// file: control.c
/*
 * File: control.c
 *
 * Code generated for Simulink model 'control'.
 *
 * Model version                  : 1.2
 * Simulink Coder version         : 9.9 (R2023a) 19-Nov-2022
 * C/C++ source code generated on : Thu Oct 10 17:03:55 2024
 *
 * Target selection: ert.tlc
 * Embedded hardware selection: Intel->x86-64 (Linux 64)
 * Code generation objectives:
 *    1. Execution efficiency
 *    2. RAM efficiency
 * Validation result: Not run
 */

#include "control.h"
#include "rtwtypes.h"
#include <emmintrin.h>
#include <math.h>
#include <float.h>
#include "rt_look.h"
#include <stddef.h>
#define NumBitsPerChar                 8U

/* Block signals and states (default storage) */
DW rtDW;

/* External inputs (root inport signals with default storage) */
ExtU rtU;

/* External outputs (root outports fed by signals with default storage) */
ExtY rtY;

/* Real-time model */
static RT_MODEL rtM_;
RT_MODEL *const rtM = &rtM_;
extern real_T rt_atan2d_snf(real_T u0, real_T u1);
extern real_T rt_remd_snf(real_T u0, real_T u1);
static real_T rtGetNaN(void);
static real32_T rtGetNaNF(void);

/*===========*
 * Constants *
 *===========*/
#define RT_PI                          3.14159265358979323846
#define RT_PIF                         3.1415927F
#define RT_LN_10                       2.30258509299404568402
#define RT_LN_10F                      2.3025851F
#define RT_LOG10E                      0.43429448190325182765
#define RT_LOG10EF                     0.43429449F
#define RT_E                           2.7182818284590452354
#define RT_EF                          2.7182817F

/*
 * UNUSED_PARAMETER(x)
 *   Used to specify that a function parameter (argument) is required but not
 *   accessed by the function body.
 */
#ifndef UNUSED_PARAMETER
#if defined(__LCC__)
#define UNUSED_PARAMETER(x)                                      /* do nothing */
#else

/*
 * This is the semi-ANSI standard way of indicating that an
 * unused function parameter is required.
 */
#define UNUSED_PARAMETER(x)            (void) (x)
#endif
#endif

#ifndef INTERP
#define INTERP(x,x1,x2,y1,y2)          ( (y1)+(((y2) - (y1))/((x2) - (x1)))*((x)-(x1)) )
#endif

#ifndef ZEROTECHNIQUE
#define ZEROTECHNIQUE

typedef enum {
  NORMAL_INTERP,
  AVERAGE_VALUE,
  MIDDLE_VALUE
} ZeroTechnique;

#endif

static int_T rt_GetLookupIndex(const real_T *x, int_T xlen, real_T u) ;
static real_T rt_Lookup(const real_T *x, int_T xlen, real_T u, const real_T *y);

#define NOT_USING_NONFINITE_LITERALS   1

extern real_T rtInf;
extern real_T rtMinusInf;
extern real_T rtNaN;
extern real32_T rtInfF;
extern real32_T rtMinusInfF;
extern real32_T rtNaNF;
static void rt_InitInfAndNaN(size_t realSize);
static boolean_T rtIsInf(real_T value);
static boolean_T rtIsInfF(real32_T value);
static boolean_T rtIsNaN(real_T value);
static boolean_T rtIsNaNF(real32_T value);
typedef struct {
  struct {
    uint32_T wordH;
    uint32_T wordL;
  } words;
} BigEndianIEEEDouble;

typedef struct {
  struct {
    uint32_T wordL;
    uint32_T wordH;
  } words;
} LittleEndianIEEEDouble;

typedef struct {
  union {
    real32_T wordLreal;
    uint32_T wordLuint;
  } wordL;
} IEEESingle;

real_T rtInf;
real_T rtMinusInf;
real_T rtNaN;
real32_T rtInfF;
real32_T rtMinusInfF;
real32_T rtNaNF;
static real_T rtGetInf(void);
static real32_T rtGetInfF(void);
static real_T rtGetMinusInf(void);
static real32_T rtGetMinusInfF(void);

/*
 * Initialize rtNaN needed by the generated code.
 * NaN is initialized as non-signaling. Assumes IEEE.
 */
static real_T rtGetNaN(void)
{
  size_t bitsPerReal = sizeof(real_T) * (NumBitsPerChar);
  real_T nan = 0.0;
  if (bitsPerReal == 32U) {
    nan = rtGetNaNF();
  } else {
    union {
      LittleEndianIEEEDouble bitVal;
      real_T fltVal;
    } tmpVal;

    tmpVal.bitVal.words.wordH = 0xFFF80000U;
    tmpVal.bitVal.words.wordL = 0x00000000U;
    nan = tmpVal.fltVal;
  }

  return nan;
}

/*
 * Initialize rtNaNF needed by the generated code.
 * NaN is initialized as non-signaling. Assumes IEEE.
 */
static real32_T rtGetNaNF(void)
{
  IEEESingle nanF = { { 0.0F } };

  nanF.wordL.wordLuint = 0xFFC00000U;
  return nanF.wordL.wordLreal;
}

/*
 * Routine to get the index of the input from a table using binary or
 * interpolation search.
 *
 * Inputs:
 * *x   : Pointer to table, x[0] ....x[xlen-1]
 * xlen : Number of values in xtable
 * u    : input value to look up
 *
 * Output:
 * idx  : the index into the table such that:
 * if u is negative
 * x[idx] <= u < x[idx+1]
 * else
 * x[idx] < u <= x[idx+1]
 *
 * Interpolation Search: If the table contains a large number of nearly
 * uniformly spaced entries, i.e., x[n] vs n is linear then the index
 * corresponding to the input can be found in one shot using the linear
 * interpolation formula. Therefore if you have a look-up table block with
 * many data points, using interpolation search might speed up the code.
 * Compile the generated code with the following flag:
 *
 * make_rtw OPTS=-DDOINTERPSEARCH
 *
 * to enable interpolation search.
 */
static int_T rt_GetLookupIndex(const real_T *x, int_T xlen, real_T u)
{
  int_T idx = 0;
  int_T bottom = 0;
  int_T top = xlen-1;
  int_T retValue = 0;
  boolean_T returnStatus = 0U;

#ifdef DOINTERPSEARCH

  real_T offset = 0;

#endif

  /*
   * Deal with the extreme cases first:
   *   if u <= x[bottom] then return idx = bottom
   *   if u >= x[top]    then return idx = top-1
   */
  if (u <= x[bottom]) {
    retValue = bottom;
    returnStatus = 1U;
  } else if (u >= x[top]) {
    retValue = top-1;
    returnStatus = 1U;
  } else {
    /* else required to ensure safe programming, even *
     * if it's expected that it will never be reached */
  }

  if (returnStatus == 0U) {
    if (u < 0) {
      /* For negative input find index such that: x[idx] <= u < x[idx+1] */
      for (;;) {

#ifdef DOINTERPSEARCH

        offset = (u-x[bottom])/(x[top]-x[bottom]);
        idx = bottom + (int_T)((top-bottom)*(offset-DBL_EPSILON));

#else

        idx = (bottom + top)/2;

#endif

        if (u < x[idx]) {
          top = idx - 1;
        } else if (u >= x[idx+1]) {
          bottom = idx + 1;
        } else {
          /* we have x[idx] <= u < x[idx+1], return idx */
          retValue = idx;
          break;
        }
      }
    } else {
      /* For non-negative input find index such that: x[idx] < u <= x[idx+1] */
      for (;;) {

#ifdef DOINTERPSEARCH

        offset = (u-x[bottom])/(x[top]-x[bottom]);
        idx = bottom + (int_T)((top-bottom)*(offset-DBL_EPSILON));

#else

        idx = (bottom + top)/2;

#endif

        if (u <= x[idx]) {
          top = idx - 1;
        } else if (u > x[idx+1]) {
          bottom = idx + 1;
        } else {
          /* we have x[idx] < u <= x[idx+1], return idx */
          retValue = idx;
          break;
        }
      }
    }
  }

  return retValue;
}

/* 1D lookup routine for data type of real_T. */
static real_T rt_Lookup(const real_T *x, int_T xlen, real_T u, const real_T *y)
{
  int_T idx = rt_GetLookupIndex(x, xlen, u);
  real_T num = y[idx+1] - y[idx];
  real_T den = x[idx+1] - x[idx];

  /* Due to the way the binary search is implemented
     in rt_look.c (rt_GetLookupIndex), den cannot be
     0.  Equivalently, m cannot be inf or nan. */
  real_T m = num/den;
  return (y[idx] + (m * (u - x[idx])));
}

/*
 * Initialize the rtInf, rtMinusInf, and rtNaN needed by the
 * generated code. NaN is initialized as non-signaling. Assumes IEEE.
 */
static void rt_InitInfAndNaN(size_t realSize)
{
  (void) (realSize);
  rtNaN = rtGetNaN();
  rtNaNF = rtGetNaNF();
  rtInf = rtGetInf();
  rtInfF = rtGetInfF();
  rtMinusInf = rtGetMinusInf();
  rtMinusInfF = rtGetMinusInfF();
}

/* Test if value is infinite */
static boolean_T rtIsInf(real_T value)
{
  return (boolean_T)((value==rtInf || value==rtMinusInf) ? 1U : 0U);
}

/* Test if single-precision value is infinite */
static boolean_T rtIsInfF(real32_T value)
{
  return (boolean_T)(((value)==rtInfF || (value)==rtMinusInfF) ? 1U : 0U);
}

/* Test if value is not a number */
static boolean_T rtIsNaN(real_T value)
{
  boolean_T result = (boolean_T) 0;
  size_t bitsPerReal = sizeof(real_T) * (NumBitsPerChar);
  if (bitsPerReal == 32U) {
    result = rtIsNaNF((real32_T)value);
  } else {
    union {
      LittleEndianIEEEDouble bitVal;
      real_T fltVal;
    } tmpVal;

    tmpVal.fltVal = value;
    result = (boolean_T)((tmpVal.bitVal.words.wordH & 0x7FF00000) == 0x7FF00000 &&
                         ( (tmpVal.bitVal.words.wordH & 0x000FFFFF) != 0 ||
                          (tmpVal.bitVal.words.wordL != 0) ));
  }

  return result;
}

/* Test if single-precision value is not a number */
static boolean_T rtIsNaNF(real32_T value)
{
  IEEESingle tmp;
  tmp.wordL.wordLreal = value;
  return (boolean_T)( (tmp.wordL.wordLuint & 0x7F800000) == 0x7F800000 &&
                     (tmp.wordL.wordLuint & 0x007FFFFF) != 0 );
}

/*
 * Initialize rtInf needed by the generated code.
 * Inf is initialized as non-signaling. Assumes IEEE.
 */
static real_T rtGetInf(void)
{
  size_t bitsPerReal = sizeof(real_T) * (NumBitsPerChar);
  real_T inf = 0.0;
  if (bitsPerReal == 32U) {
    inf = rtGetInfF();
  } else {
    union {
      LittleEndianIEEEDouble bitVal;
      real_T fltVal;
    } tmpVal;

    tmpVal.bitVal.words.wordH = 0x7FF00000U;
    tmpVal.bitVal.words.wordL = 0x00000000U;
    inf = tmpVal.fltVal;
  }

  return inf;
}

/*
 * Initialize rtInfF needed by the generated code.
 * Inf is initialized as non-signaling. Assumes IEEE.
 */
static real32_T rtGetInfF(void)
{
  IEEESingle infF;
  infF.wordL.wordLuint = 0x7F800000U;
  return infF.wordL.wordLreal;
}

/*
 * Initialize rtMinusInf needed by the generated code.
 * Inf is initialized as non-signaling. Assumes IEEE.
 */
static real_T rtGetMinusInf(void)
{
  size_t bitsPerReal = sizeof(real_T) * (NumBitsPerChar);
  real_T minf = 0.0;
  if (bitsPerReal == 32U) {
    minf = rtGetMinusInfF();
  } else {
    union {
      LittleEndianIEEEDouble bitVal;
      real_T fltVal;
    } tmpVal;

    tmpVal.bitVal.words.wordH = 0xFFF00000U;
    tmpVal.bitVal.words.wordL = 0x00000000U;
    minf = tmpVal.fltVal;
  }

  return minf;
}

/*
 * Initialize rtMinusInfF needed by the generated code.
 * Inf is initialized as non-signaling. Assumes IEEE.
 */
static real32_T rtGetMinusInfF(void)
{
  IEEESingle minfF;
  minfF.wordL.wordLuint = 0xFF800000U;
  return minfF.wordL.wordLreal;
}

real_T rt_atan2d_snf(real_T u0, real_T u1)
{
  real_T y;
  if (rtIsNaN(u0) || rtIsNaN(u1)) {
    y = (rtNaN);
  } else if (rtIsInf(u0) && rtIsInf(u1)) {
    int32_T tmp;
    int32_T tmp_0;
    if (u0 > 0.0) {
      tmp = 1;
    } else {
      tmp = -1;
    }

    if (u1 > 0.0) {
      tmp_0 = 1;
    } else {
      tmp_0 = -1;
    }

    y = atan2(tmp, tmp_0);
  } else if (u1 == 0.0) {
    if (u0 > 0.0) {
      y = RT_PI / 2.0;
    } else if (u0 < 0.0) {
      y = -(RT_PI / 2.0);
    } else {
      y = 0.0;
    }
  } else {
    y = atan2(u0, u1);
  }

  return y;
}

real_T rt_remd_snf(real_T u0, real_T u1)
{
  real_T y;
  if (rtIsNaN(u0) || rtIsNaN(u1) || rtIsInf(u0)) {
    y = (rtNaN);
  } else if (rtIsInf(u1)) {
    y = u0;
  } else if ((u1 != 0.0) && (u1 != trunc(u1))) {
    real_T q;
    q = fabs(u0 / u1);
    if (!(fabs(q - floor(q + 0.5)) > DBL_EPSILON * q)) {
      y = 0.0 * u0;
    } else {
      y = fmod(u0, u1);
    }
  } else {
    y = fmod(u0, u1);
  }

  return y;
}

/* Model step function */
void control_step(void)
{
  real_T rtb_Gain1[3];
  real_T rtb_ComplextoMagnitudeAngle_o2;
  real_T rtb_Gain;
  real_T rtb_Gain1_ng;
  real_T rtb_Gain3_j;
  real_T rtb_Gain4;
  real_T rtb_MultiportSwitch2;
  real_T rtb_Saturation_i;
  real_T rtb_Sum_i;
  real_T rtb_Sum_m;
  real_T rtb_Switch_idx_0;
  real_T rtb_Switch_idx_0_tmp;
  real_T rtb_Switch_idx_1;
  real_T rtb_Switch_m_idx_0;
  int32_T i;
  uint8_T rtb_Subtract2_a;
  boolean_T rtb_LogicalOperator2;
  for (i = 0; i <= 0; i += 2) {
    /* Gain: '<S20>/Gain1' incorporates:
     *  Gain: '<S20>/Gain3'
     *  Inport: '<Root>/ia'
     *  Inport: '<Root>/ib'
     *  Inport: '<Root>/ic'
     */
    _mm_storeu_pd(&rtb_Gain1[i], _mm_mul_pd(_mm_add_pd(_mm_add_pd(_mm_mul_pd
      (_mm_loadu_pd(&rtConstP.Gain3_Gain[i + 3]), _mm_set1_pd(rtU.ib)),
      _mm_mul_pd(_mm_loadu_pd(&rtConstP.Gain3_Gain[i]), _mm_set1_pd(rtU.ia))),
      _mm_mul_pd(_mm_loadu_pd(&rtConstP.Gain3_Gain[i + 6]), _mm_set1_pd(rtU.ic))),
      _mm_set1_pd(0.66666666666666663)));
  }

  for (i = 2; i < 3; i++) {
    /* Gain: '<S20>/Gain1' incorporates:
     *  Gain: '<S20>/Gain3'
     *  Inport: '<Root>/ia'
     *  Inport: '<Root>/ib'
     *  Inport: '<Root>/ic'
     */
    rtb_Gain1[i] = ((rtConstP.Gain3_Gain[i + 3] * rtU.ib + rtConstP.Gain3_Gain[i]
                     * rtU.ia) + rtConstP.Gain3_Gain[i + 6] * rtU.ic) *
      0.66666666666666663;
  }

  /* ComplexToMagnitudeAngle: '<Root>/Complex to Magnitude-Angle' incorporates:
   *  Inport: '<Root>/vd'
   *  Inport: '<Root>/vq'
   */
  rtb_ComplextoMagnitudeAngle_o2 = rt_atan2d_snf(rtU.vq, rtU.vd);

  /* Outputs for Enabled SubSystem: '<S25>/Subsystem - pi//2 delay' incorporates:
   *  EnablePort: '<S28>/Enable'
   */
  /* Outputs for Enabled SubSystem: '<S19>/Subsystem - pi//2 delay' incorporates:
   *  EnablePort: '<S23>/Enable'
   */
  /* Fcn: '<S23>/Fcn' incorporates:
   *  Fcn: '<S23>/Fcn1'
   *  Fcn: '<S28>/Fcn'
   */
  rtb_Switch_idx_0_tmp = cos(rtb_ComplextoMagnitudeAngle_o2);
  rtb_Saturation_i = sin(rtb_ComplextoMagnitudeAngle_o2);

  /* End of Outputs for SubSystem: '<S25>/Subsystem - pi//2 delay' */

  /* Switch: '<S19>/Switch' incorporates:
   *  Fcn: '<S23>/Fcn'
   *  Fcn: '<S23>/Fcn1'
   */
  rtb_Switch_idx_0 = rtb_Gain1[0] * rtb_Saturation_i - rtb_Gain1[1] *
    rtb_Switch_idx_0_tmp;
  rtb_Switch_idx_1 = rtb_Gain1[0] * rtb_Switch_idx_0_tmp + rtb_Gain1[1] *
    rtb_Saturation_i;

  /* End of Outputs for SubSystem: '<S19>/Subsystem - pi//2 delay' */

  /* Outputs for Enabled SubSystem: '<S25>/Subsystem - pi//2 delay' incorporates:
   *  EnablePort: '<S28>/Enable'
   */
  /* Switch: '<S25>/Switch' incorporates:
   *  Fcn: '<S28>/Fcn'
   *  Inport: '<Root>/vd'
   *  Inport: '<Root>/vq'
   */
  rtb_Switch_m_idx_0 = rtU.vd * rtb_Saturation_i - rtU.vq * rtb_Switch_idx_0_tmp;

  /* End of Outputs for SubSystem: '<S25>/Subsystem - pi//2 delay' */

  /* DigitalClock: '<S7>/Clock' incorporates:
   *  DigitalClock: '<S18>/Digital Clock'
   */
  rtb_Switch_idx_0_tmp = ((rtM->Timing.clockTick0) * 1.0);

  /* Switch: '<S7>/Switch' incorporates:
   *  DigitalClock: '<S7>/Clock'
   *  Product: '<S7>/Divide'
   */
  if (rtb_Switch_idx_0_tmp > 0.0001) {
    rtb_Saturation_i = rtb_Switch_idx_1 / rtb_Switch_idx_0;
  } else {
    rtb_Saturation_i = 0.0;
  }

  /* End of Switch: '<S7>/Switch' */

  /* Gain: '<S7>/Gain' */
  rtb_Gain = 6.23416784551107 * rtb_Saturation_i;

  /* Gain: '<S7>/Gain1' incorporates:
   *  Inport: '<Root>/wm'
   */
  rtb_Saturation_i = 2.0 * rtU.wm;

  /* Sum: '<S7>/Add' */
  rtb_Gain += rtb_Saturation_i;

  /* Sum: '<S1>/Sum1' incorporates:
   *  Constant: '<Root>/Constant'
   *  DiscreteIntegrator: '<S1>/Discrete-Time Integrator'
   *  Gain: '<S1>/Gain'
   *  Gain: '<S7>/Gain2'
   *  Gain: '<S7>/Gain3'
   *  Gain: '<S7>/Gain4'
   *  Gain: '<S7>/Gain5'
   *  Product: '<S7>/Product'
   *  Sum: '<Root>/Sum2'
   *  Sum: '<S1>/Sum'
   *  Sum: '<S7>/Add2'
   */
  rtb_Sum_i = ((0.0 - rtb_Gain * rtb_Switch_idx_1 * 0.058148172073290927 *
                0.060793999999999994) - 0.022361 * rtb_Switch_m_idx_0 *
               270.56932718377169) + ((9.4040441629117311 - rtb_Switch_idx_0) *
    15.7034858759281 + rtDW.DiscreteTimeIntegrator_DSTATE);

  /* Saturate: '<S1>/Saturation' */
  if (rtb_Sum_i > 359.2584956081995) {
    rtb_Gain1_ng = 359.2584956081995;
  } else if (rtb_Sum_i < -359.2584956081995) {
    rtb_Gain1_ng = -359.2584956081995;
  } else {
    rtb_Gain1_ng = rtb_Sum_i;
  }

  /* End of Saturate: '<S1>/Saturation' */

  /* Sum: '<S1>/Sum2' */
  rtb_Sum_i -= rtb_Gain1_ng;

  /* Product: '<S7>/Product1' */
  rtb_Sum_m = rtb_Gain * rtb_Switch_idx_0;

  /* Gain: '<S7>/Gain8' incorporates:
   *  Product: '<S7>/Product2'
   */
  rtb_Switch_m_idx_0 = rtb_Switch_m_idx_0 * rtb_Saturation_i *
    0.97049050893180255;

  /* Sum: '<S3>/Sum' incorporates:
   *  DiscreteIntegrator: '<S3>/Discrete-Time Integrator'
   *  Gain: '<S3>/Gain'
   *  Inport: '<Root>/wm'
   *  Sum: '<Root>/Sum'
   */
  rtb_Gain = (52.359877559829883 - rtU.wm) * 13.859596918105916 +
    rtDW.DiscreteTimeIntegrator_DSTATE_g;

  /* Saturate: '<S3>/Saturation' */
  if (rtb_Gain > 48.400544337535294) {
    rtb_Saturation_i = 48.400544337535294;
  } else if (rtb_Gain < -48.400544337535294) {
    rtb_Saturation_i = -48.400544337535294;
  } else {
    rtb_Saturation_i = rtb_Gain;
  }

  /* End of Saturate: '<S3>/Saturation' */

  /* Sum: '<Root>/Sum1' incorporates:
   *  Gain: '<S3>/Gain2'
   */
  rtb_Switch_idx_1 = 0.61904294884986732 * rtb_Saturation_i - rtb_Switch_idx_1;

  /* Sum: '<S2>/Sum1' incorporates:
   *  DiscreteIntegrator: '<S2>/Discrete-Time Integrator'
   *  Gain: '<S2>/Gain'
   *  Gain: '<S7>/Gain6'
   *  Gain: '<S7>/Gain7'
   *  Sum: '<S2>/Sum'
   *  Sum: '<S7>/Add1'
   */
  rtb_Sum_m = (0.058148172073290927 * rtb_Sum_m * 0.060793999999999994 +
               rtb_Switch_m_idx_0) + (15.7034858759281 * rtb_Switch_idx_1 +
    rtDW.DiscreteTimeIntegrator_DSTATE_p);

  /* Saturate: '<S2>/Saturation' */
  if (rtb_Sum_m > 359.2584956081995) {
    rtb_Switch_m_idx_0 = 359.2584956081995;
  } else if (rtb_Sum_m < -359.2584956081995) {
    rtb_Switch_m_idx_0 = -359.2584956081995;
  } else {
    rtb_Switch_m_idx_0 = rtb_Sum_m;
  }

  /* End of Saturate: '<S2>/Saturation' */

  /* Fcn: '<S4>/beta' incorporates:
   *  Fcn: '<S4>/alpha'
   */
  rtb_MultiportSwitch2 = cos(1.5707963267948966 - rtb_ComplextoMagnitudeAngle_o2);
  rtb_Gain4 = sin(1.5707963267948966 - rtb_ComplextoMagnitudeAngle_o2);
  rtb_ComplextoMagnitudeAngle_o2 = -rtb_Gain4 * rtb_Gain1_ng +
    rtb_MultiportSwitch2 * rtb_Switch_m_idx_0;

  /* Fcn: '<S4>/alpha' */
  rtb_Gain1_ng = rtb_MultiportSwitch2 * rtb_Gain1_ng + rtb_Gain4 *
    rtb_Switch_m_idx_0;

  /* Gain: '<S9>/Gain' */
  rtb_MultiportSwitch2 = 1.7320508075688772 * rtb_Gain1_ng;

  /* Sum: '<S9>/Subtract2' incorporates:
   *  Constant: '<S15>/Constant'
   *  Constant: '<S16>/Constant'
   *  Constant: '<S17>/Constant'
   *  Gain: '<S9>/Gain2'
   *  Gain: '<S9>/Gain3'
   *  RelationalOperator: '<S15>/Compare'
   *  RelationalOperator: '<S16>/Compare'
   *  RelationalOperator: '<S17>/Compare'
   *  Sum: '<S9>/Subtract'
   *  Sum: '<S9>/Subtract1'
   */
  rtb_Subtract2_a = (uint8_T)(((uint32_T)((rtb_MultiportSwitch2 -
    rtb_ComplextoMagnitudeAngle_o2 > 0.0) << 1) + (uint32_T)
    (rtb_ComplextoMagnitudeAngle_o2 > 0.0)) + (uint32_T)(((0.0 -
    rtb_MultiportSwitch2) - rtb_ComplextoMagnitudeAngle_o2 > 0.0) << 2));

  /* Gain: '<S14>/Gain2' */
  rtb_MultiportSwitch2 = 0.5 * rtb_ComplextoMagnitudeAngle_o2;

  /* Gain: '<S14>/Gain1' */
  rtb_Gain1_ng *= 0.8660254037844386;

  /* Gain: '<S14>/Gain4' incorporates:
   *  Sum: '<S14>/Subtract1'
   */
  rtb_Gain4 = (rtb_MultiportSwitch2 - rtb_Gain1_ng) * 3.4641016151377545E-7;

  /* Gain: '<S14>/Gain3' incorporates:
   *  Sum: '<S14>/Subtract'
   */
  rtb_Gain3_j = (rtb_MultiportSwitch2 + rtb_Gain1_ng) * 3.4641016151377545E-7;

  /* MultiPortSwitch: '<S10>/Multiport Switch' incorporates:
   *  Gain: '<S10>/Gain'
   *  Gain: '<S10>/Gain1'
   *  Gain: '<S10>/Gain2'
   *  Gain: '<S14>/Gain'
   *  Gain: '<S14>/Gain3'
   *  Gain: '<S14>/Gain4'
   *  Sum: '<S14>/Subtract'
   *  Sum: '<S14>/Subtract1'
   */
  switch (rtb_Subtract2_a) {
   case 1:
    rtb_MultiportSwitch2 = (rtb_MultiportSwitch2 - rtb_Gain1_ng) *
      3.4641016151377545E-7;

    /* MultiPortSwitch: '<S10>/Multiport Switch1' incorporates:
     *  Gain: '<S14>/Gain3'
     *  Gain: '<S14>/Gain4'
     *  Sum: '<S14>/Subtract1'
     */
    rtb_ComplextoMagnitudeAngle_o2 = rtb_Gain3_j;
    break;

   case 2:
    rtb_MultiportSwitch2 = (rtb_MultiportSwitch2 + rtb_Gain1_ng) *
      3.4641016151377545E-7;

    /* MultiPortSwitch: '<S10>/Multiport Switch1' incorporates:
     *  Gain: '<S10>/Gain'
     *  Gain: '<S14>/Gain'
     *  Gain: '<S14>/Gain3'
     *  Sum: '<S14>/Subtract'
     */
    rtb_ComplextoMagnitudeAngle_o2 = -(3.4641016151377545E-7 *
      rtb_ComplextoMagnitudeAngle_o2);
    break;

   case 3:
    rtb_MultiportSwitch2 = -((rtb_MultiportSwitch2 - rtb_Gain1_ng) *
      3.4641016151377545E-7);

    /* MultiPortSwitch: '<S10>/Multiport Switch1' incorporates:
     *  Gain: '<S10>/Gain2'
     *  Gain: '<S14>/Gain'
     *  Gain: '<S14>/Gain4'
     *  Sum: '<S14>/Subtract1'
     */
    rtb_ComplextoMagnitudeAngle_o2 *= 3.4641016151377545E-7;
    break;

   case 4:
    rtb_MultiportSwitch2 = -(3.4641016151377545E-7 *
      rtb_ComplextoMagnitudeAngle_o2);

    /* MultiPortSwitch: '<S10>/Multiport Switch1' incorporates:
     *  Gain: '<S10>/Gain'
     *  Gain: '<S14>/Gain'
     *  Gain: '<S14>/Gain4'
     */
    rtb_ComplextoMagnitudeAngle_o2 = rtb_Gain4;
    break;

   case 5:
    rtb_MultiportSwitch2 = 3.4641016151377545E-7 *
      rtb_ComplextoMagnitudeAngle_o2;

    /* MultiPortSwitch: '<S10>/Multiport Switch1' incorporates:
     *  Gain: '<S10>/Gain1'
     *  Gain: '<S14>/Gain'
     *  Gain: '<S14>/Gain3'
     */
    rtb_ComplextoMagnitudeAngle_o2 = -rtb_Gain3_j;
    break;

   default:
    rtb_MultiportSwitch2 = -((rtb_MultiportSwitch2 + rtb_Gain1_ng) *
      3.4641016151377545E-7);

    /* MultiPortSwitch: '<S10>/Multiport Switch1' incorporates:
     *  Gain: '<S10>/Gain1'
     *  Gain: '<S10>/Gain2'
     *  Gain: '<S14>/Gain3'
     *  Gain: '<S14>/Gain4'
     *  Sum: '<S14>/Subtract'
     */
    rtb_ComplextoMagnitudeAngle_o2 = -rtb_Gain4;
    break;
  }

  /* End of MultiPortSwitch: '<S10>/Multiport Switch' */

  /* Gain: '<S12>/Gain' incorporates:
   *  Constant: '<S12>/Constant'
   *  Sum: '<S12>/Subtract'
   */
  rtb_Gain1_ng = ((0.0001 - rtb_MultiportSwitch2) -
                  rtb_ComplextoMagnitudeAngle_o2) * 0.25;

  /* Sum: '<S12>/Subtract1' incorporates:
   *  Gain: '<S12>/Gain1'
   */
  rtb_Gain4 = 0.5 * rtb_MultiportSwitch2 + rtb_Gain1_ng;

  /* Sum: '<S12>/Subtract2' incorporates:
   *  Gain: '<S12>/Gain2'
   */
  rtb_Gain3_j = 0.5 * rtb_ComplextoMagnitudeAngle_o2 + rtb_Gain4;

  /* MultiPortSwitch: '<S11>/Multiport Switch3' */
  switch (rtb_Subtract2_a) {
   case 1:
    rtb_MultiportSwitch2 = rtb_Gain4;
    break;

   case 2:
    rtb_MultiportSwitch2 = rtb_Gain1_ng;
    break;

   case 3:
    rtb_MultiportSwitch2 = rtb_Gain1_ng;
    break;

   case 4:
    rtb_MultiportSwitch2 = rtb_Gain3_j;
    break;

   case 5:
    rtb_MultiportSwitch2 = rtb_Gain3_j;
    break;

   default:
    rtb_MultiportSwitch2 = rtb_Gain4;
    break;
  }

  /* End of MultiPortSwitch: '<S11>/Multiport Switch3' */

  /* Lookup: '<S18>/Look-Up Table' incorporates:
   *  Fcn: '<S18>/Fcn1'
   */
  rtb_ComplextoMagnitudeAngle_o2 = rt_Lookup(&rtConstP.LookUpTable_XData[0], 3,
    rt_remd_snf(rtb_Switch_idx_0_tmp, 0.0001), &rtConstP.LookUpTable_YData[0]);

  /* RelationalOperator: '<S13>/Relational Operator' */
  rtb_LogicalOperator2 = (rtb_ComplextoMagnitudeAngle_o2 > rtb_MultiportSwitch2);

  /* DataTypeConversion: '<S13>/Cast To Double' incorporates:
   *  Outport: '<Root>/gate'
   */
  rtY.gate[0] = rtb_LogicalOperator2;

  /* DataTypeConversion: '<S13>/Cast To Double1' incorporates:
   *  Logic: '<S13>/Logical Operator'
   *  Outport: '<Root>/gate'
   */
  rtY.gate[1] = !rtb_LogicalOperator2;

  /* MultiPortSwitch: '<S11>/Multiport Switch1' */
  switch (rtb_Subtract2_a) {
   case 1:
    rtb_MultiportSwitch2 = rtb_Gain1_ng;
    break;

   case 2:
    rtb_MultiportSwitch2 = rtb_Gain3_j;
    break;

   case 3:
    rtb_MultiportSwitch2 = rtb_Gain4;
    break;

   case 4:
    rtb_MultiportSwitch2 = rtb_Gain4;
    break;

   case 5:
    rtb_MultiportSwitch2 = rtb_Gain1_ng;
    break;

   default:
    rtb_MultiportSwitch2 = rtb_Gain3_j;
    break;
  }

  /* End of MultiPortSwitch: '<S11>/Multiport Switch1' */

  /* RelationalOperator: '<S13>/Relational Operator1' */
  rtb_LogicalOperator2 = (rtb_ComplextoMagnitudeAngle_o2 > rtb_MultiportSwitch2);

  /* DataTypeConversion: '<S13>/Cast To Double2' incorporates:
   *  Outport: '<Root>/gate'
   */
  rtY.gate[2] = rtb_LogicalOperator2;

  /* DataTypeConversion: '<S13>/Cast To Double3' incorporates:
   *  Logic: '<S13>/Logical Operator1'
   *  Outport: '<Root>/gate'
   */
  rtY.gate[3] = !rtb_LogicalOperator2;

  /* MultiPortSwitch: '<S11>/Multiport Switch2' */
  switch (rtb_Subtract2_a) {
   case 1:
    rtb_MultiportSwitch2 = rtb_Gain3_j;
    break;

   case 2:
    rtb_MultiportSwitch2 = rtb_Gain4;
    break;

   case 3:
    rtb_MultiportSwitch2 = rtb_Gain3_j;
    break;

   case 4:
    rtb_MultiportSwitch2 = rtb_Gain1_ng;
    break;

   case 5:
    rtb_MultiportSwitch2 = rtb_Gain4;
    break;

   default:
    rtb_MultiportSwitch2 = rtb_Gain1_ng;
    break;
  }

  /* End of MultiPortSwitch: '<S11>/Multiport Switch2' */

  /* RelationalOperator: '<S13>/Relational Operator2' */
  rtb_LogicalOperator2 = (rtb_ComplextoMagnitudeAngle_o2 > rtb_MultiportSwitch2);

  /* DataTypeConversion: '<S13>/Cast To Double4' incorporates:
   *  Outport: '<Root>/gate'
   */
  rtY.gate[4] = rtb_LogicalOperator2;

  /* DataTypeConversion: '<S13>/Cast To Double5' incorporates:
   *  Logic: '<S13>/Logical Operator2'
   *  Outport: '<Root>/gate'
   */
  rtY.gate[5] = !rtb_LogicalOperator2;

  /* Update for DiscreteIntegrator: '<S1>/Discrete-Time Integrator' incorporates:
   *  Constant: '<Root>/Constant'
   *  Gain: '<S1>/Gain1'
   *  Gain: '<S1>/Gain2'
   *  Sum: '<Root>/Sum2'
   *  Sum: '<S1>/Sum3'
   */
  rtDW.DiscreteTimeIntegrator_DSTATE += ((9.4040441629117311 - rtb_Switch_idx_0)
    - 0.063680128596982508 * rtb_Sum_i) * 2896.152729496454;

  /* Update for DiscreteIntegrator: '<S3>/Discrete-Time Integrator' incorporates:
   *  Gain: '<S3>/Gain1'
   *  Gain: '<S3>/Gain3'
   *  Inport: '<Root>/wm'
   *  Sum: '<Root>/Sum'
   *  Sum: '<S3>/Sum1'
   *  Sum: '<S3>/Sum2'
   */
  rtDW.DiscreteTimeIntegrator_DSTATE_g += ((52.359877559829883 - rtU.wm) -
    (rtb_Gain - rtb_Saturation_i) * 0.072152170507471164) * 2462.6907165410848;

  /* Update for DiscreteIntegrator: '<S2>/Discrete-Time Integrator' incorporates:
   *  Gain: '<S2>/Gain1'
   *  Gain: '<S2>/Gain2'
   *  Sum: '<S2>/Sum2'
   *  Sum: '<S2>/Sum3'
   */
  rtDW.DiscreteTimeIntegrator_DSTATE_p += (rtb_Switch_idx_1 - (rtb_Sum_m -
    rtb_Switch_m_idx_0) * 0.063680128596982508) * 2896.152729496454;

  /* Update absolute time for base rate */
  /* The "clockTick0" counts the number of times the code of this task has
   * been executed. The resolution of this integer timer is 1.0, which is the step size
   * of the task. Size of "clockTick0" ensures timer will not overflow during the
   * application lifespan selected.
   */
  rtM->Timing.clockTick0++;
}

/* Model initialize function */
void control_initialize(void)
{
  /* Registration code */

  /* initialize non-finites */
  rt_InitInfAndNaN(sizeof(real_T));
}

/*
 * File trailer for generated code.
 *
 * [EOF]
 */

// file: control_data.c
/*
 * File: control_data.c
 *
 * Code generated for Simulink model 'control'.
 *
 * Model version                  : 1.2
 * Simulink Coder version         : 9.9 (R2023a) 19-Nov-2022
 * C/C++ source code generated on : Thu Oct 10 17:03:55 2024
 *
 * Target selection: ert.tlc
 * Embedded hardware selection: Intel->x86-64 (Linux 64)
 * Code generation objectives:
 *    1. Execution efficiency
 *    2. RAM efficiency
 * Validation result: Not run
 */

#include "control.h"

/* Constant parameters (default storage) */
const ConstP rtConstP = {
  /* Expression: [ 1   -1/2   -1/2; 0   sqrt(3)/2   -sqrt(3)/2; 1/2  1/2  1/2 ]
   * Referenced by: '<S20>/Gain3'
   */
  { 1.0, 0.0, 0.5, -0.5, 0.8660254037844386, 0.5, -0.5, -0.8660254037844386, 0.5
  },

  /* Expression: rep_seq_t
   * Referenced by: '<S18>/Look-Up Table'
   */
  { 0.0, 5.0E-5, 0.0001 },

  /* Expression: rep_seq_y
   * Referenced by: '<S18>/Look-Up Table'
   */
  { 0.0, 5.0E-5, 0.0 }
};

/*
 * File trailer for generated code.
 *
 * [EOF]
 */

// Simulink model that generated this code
simulink model "control"  (R2023a)
settings: Solver=FixedStepDiscrete  StartTime=0.0  StopTime=10.0  RelTol=1e-3
undefined symbols (not defined in the file): DiscIntNeverNeededParam, Ids_rated, Kac, Kas, Kic, Kis, Kpc, Kps, Kt, Lm, Lr, Ls, np, pxyz, Rr, sigma, tau_r, Te_rated, Tsw, V_max
libraries: simulink x3, eeTransforms x1, discretizing x1, spsabctodq0Lib x1, spsAlphaBetaZerotodq0Lib x1, spspowerguiLib x1

== system control ==
  ia : Inport
  ib : Inport  Port=2
  ic : Inport  Port=3
  vd : Inport  Port=4
  vq : Inport  Port=5
  wm : Inport  Port=6
  ACR_d : Subsystem
  ACR_q : Subsystem
  ASR : Subsystem
  Complex to Magnitude-Angle : ComplexToMagnitudeAngle
  Constant : Constant  Value=Ids_rated
  Constant1 : Constant  Value=500
  Demux : Demux  Outputs=3
  Demux1 : Demux  Outputs=3
  Gain1 : Gain  Gain=pi/30
  Ground : Ground
  Mux : Mux  Inputs=3
  Mux1 : Mux  Inputs=3
  Park to Clarke Angle Transform : eeTransforms/Park to Clarke Angle Transform  AxisAlignment=Q-axis
  Real-Imag to Complex : RealImagToComplex
  SVPWM : Subsystem
  Sum : Sum  Inputs=|+-
  Sum1 : Sum  Inputs=|+-
  Sum2 : Sum  Inputs=|+-
  Terminator : Terminator
  Terminator1 : Terminator
  Terminator2 : Terminator
  abc to dq0 : spsabctodq0Lib/abc to dq0  Alignment=90 degrees behind phase A axis
  feedforward : Subsystem
  powergui : spspowerguiLib/powergui  Priority=1  SimulationMode=Discrete  SampleTime=Tsw / 10  frequency=60  Iterations=50  frequencyindice=50  Pbase=100e6  ErrMax=1e-4  UnitsV=kV  UnitsW=MW  buscounter=0  FunctionMessages=off  echomessages=off  EnableUseOfTLC=off  CurrentSourceSwitches=off  DisableSnubberDevices=off  DisableRonSwitches=off  DisableVfSwitches=off  DisplayEquations=off  AutomaticDiscreteSolvers=off  SolverType=Tustin/Backward Euler (TBE)  Interpol=off  ExternalGateDelay=off  methode=off  Ts=100  x0status=blocks  SPID=on  SwTol=0  HookPort=off  NonlinearTolerance=1e-4  nMaxIteration=100  ContinueOnMaxIteration=off  RestoreLinks=warning  ResistiveCurrentMeasurement=off  Frange=[0:2:500]  Ylog=off  Xlog=on  ShowGrid=off  save=off  variable=ZData  structure=0  ZoomFFT=off  StartTime=0.0  cycles=1  DisplayStyle=1  fundamental=60  FreqAxis=off  MaxFrequency=1000  frequencyindicesteady=1  RmsSteady=1  display=off
  gate : Outport
  wires:
  Park to Clarke Angle Transform/1 -> Demux1/1
  ACR_q/1(Vq*) -> Mux/2
  Gain1/1 -> Sum/1
  Sum/1 -> ASR/1(e_wm)
  [flux_q] -> feedforward/4(flux_q)
  Mux/1 -> Park to Clarke Angle Transform/1
  [iqs] -> feedforward/2(iqs)
  ACR_d/1(Vd*) -> Mux/1
  Sum1/1 -> ACR_q/1(e_iqs)
  SVPWM/1(g) -> gate/1
  [ids] -> feedforward/1(ids)
  Demux1/3 -> Terminator/1
  Demux1/2 -> SVPWM/2(beta)
  Demux/3 -> Terminator2/1
  feedforward/2(vq_ff) -> [vq_ff]
  [wm] -> Sum/2
  Demux1/1 -> SVPWM/1(alpha)
  ib/1 -> Mux1/2
  Ground/1 -> Mux/3
  Sum2/1 -> ACR_d/1(e_ids)
  Constant1/1 -> Gain1/1
  [iqs] -> Sum1/2
  [vq_ff] -> ACR_q/2(vq_ff)
  Mux1/1 -> abc to dq0/1
  ASR/1(iqs*) -> Sum1/1
  Constant/1 -> Sum2/1
  Demux/1 -> [ids]
  feedforward/1(vd_ff) -> [vd_ff]
  [vd_ff] -> ACR_d/2(vd_ff)
  vq/1 -> [flux_q], Real-Imag to Complex/2
  Demux/2 -> [iqs]
  ia/1 -> Mux1/1
  [ids] -> Sum2/2
  abc to dq0/1 -> Demux/1
  Complex to Magnitude-Angle/2 -> feedforward/5(theta), Park to Clarke Angle Transform/2, abc to dq0/2
  [flux_d] -> feedforward/3(flux_d)
  Real-Imag to Complex/1 -> Complex to Magnitude-Angle/1
  wm/1 -> [wm]
  Complex to Magnitude-Angle/1 -> Terminator1/1
  vd/1 -> Real-Imag to Complex/1, [flux_d]
  ic/1 -> Mux1/3
  [wm] -> feedforward/6(wm)

== system control/ACR_d ==
  e_ids : Inport
  vd_ff : Inport  Port=2
  Discrete-Time Integrator : DiscreteIntegrator  SampleTime=-1  ICPrevOutput=DiscIntNeverNeededParam  ICPrevScaledInput=DiscIntNeverNeededParam
  Gain : Gain  Gain=Kpc
  Gain1 : Gain  Gain=Kic
  Gain2 : Gain  Gain=Kac
  Saturation : Saturate  UpperLimit=V_max * 2  LowerLimit=-V_max * 2
  Sum : Sum  Inputs=|++
  Sum1 : Sum  Inputs=++|
  Sum2 : Sum  Inputs=+-|
  Sum3 : Sum  Inputs=+|-
  Vd* : Outport
  wires:
  e_ids/1 -> Sum3/1, Gain/1
  Gain1/1 -> Discrete-Time Integrator/1
  Gain/1 -> Sum/1
  Discrete-Time Integrator/1 -> Sum/2
  Sum/1 -> Sum1/2
  vd_ff/1 -> Sum1/1
  Sum1/1 -> Saturation/1, Sum2/1
  Saturation/1 -> Sum2/2, Vd*/1
  Sum2/1 -> Gain2/1
  Sum3/1 -> Gain1/1
  Gain2/1 -> Sum3/2

== system control/ACR_q ==
  e_iqs : Inport
  vq_ff : Inport  Port=2
  Discrete-Time Integrator : DiscreteIntegrator  SampleTime=-1  ICPrevOutput=DiscIntNeverNeededParam  ICPrevScaledInput=DiscIntNeverNeededParam
  Gain : Gain  Gain=Kpc
  Gain1 : Gain  Gain=Kic
  Gain2 : Gain  Gain=Kac
  Saturation : Saturate  UpperLimit=V_max * 2  LowerLimit=-V_max * 2
  Sum : Sum  Inputs=|++
  Sum1 : Sum  Inputs=++|
  Sum2 : Sum  Inputs=+-|
  Sum3 : Sum  Inputs=+|-
  Vq* : Outport
  wires:
  e_iqs/1 -> Sum3/1, Gain/1
  Gain1/1 -> Discrete-Time Integrator/1
  Gain/1 -> Sum/1
  Discrete-Time Integrator/1 -> Sum/2
  Sum/1 -> Sum1/2
  vq_ff/1 -> Sum1/1
  Sum1/1 -> Saturation/1, Sum2/1
  Saturation/1 -> Sum2/2, Vq*/1
  Sum2/1 -> Gain2/1
  Sum3/1 -> Gain1/1
  Gain2/1 -> Sum3/2

== system control/ASR ==
  e_wm : Inport
  Discrete-Time Integrator : DiscreteIntegrator  SampleTime=-1  ICPrevOutput=DiscIntNeverNeededParam  ICPrevScaledInput=DiscIntNeverNeededParam
  Gain : Gain  Gain=Kps
  Gain1 : Gain  Gain=Kis
  Gain2 : Gain  Gain=1/Kt
  Gain3 : Gain  Gain=Kas
  Saturation : Saturate  UpperLimit=Te_rated  LowerLimit=-Te_rated
  Sum : Sum  Inputs=|++
  Sum1 : Sum  Inputs=+-|
  Sum2 : Sum  Inputs=+|-
  iqs* : Outport
  wires:
  e_wm/1 -> Sum2/1, Gain/1
  Gain1/1 -> Discrete-Time Integrator/1
  Gain/1 -> Sum/1
  Discrete-Time Integrator/1 -> Sum/2
  Sum/1 -> Sum1/1, Saturation/1
  Saturation/1 -> Sum1/2, Gain2/1
  Gain2/1 -> iqs*/1
  Sum1/1 -> Gain3/1
  Sum2/1 -> Gain1/1
  Gain3/1 -> Sum2/2

== system control/SVPWM ==
  alpha : Inport
  beta : Inport  Port=2
  Sector : Subsystem
  T1T2 : Subsystem
  allocate : Subsystem
  fuse : Subsystem
  gating : Subsystem
  xyz : Subsystem
  g : Outport
  wires:
  allocate/3(C) -> gating/3(C)
  fuse/2(Tb) -> allocate/3(Tb)
  allocate/1(A) -> gating/1(A)
  allocate/2(B) -> gating/2(B)
  xyz/2(y) -> T1T2/3(y)
  T1T2/1(T1) -> fuse/1(T1)
  xyz/3(z) -> T1T2/4(z)
  T1T2/2(T2) -> fuse/2(T2)
  fuse/3(Tc) -> allocate/4(Tc)
  Sector/1(N) -> T1T2/1(N), allocate/1(N)
  fuse/1(Ta) -> allocate/2(Ta)
  xyz/1(x) -> T1T2/2(X)
  alpha/1 -> Sector/1(alpha), xyz/1(alpha)
  beta/1 -> Sector/2(beta), xyz/2(beta)
  gating/1(g) -> g/1

== system control/feedforward ==
  ids : Inport
  iqs : Inport  Port=2
  flux_d : Inport  Port=3
  flux_q : Inport  Port=4
  theta : Inport  Port=5
  wm : Inport  Port=6
  Add : Sum  Inputs=|++
  Add1 : Sum
  Add2 : Sum  Inputs=--
  Alpha-Beta-Zero to dq0 : spsAlphaBetaZerotodq0Lib/Alpha-Beta-Zero to dq0  Alignment=90 degrees behind phase A axis
  Clock : DigitalClock  SampleTime=1.0
  Demux : Demux  Outputs=3
  Divide : Product  Inputs=*/
  Gain : Gain  Gain=1/tau_r
  Gain1 : Gain  Gain=np
  Gain2 : Gain  Gain=sigma
  Gain3 : Gain  Gain=Ls
  Gain4 : Gain  Gain=Rr * Lm
  Gain5 : Gain  Gain=1 / (Lr ^ 2)
  Gain6 : Gain  Gain=sigma
  Gain7 : Gain  Gain=Ls
  Gain8 : Gain  Gain=Lm / Lr
  Ground : Ground
  Ground1 : Ground
  Mux : Mux  Inputs=3
  Product : Product
  Product1 : Product
  Product2 : Product
  Switch : Switch  Criteria=u2 > Threshold  Threshold=Tsw  SaturateOnIntegerOverflow=off  InputSameDT=off
  Terminator : Terminator
  Terminator1 : Terminator
  vd_ff : Outport
  vq_ff : Outport  Port=2
  wires:
  Divide/1 -> Switch/1
  Switch/1 -> Gain/1
  Ground/1 -> Switch/3
  wm/1 -> Gain1/1
  Gain/1 -> Add/1
  Gain1/1 -> [wr], Add/2
  Add/1 -> [we]
  iqs/1 -> [iqs], Divide/1
  ids/1 -> [ids], Divide/2
  flux_d/1 -> Mux/1
  flux_q/1 -> Mux/2
  Ground1/1 -> Mux/3
  Mux/1 -> Alpha-Beta-Zero to dq0/1
  Alpha-Beta-Zero to dq0/1 -> Demux/1
  Demux/3 -> Terminator/1
  theta/1 -> Alpha-Beta-Zero to dq0/2
  Demux/2 -> Terminator1/1
  [we] -> Product/1
  [iqs] -> Product/2
  Product/1 -> Gain2/1
  Gain2/1 -> Gain3/1
  Gain4/1 -> Gain5/1
  Demux/1 -> Product2/1, Gain4/1  "λd"
  Gain3/1 -> Add2/1
  Add2/1 -> vd_ff/1
  Gain5/1 -> Add2/2
  [we] -> Product1/1
  [ids] -> Product1/2
  Product1/1 -> Gain6/1
  Gain6/1 -> Gain7/1
  Add1/1 -> vq_ff/1
  Gain7/1 -> Add1/1
  [wr] -> Product2/2
  Product2/1 -> Gain8/1
  Gain8/1 -> Add1/2
  Clock/1 -> Switch/2

== system control/SVPWM/Sector ==
  alpha : Inport
  beta : Inport  Port=2
  Gain : Gain  Gain=sqrt(3)
  Gain1 : Gain
  Gain2 : Gain  Gain=2
  Gain3 : Gain  Gain=4
  Subtract : Sum  Inputs=+-
  Subtract1 : Sum  Inputs=--
  Subtract2 : Sum  Inputs=+++
  准则A : simulink/Logic and Bit Operations/Compare To Constant  relop=>  const=0  OutDataTypeStr=boolean
  准则B : simulink/Logic and Bit Operations/Compare To Constant  relop=>  const=0  OutDataTypeStr=boolean
  准则C : simulink/Logic and Bit Operations/Compare To Constant  relop=>  const=0  OutDataTypeStr=boolean
  N : Outport
  wires:
  beta/1 -> Subtract1/2, Subtract/2, 准则A/1
  alpha/1 -> Gain/1
  Gain/1 -> Subtract1/1, Subtract/1
  Subtract/1 -> 准则B/1
  Subtract1/1 -> 准则C/1
  准则C/1 -> Gain3/1
  准则B/1 -> Gain2/1
  准则A/1 -> Gain1/1
  Gain1/1 -> Subtract2/1
  Gain2/1 -> Subtract2/2
  Gain3/1 -> Subtract2/3
  Subtract2/1 -> N/1

== system control/SVPWM/T1T2 ==
  N : Inport
  X : Inport  Port=2
  y : Inport  Port=3
  z : Inport  Port=4
  Gain : Gain  Gain=-1
  Gain1 : Gain  Gain=-1
  Gain2 : Gain  Gain=-1
  Multiport Switch : MultiPortSwitch  Inputs=6  SaturateOnIntegerOverflow=off  InputSameDT=off
  Multiport Switch1 : MultiPortSwitch  Inputs=6  SaturateOnIntegerOverflow=off  InputSameDT=off
  T1 : Outport
  T2 : Outport  Port=2
  wires:
  X/1 -> [pX], Gain/1
  y/1 -> [pY], Gain1/1
  z/1 -> Gain2/1, [pZ]
  Gain/1 -> [nX]
  Gain1/1 -> [nY]
  Gain2/1 -> [nZ]
  Multiport Switch/1 -> T1/1
  Multiport Switch1/1 -> T2/1
  N/1 -> Multiport Switch1/1, Multiport Switch/1
  [pZ] -> Multiport Switch/2
  [pY] -> Multiport Switch/3
  [nZ] -> Multiport Switch/4
  [nX] -> Multiport Switch/5
  [pX] -> Multiport Switch/6
  [nY] -> Multiport Switch/7
  [pY] -> Multiport Switch1/2
  [nX] -> Multiport Switch1/3
  [pX] -> Multiport Switch1/4
  [pZ] -> Multiport Switch1/5
  [nY] -> Multiport Switch1/6
  [nZ] -> Multiport Switch1/7

== system control/SVPWM/allocate ==
  N : Inport
  Ta : Inport  Port=2
  Tb : Inport  Port=3
  Tc : Inport  Port=4
  Multiport Switch1 : MultiPortSwitch  Inputs=6  SaturateOnIntegerOverflow=off  InputSameDT=off
  Multiport Switch2 : MultiPortSwitch  Inputs=6  SaturateOnIntegerOverflow=off  InputSameDT=off
  Multiport Switch3 : MultiPortSwitch  Inputs=6  SaturateOnIntegerOverflow=off  InputSameDT=off
  A : Outport
  B : Outport  Port=2
  C : Outport  Port=3
  wires:
  Tc/1 -> [Tc]
  Tb/1 -> [Tb]
  Ta/1 -> [Ta]
  Multiport Switch2/1 -> C/1
  Multiport Switch3/1 -> A/1
  Multiport Switch1/1 -> B/1
  N/1 -> Multiport Switch3/1, Multiport Switch1/1, Multiport Switch2/1
  [Tb] -> Multiport Switch3/2
  [Ta] -> Multiport Switch1/2
  [Tc] -> Multiport Switch2/2
  [Ta] -> Multiport Switch3/3
  [Ta] -> Multiport Switch3/4
  [Tc] -> Multiport Switch3/5
  [Tc] -> Multiport Switch3/6
  [Tb] -> Multiport Switch3/7
  [Tc] -> Multiport Switch1/3
  [Tb] -> Multiport Switch1/4
  [Tb] -> Multiport Switch1/5
  [Ta] -> Multiport Switch1/6
  [Tc] -> Multiport Switch1/7
  [Tb] -> Multiport Switch2/3
  [Tc] -> Multiport Switch2/4
  [Ta] -> Multiport Switch2/5
  [Tb] -> Multiport Switch2/6
  [Ta] -> Multiport Switch2/7

== system control/SVPWM/fuse ==
  T1 : Inport
  T2 : Inport  Port=2
  Constant : Constant  Value=Tsw
  Gain : Gain  Gain=1 / 4
  Gain1 : Gain  Gain=1 / 2
  Gain2 : Gain  Gain=1 / 2
  Subtract : Sum  Inputs=+--
  Subtract1 : Sum
  Subtract2 : Sum
  Ta : Outport
  Tb : Outport  Port=2
  Tc : Outport  Port=3
  wires:
  Constant/1 -> Subtract/1
  T1/1 -> Gain1/1, Subtract/2
  T2/1 -> Gain2/1, Subtract/3
  Subtract/1 -> Gain/1
  Gain/1 -> Subtract1/1, Ta/1
  Gain1/1 -> Subtract1/2
  Subtract1/1 -> Subtract2/1, Tb/1
  Subtract2/1 -> Tc/1
  Gain2/1 -> Subtract2/2

== system control/SVPWM/gating ==
  A : Inport
  B : Inport  Port=2
  C : Inport  Port=3
  Cast To Double{,1..5} (6 alike) : DataTypeConversion  OutDataTypeStr=double  SaturateOnIntegerOverflow=off  RndMeth=Floor
  Logical Operator : Logic  Operator=NOT  AllPortsSameDT=off  OutDataTypeStr=boolean
  Logical Operator1 : Logic  Operator=NOT  AllPortsSameDT=off  OutDataTypeStr=boolean
  Logical Operator2 : Logic  Operator=NOT  AllPortsSameDT=off  OutDataTypeStr=boolean
  Relational Operator : RelationalOperator  Operator=>  OutDataTypeStr=boolean  RndMeth=Simplest  InputSameDT=off
  Relational Operator1 : RelationalOperator  Operator=>  OutDataTypeStr=boolean  RndMeth=Simplest  InputSameDT=off
  Relational Operator2 : RelationalOperator  Operator=>  OutDataTypeStr=boolean  RndMeth=Simplest  InputSameDT=off
  Vector Concatenate : Concatenate  NumInputs=6
  triangle : discretizing/Discretized Repeating Sequence  rep_seq_t=[0 Tsw/2 Tsw]  rep_seq_y=[0 Tsw/2 0]  SampleTime=1.0
  g : Outport
  wires:
  A/1 -> Relational Operator/2
  B/1 -> Relational Operator1/2
  C/1 -> Relational Operator2/2
  Relational Operator1/1 -> Cast To Double2/1, Logical Operator1/1
  Relational Operator/1 -> Cast To Double/1, Logical Operator/1
  Relational Operator2/1 -> Cast To Double4/1, Logical Operator2/1
  Logical Operator/1 -> Cast To Double1/1
  Logical Operator1/1 -> Cast To Double3/1
  Logical Operator2/1 -> Cast To Double5/1
  Cast To Double/1 -> Vector Concatenate/1
  Cast To Double1/1 -> Vector Concatenate/2
  Cast To Double2/1 -> Vector Concatenate/3
  Cast To Double3/1 -> Vector Concatenate/4
  Cast To Double4/1 -> Vector Concatenate/5
  Cast To Double5/1 -> Vector Concatenate/6
  Vector Concatenate/1 -> g/1
  triangle/1 -> Relational Operator/1, Relational Operator2/1, Relational Operator1/1

== system control/SVPWM/xyz ==
  alpha : Inport
  beta : Inport  Port=2
  Gain : Gain  Gain=pxyz
  Gain1 : Gain  Gain=sqrt(3) / 2
  Gain2 : Gain  Gain=0.5
  Gain3 : Gain  Gain=pxyz
  Gain4 : Gain  Gain=pxyz
  Subtract : Sum
  Subtract1 : Sum  Inputs=+-
  x : Outport
  y : Outport  Port=2
  z : Outport  Port=3
  wires:
  beta/1 -> Gain2/1, Gain/1
  Gain/1 -> x/1
  alpha/1 -> Gain1/1
  Gain2/1 -> Subtract1/1, Subtract/1
  Gain1/1 -> Subtract/2, Subtract1/2
  Gain3/1 -> y/1
  Subtract/1 -> Gain3/1
  Gain4/1 -> z/1
  Subtract1/1 -> Gain4/1
